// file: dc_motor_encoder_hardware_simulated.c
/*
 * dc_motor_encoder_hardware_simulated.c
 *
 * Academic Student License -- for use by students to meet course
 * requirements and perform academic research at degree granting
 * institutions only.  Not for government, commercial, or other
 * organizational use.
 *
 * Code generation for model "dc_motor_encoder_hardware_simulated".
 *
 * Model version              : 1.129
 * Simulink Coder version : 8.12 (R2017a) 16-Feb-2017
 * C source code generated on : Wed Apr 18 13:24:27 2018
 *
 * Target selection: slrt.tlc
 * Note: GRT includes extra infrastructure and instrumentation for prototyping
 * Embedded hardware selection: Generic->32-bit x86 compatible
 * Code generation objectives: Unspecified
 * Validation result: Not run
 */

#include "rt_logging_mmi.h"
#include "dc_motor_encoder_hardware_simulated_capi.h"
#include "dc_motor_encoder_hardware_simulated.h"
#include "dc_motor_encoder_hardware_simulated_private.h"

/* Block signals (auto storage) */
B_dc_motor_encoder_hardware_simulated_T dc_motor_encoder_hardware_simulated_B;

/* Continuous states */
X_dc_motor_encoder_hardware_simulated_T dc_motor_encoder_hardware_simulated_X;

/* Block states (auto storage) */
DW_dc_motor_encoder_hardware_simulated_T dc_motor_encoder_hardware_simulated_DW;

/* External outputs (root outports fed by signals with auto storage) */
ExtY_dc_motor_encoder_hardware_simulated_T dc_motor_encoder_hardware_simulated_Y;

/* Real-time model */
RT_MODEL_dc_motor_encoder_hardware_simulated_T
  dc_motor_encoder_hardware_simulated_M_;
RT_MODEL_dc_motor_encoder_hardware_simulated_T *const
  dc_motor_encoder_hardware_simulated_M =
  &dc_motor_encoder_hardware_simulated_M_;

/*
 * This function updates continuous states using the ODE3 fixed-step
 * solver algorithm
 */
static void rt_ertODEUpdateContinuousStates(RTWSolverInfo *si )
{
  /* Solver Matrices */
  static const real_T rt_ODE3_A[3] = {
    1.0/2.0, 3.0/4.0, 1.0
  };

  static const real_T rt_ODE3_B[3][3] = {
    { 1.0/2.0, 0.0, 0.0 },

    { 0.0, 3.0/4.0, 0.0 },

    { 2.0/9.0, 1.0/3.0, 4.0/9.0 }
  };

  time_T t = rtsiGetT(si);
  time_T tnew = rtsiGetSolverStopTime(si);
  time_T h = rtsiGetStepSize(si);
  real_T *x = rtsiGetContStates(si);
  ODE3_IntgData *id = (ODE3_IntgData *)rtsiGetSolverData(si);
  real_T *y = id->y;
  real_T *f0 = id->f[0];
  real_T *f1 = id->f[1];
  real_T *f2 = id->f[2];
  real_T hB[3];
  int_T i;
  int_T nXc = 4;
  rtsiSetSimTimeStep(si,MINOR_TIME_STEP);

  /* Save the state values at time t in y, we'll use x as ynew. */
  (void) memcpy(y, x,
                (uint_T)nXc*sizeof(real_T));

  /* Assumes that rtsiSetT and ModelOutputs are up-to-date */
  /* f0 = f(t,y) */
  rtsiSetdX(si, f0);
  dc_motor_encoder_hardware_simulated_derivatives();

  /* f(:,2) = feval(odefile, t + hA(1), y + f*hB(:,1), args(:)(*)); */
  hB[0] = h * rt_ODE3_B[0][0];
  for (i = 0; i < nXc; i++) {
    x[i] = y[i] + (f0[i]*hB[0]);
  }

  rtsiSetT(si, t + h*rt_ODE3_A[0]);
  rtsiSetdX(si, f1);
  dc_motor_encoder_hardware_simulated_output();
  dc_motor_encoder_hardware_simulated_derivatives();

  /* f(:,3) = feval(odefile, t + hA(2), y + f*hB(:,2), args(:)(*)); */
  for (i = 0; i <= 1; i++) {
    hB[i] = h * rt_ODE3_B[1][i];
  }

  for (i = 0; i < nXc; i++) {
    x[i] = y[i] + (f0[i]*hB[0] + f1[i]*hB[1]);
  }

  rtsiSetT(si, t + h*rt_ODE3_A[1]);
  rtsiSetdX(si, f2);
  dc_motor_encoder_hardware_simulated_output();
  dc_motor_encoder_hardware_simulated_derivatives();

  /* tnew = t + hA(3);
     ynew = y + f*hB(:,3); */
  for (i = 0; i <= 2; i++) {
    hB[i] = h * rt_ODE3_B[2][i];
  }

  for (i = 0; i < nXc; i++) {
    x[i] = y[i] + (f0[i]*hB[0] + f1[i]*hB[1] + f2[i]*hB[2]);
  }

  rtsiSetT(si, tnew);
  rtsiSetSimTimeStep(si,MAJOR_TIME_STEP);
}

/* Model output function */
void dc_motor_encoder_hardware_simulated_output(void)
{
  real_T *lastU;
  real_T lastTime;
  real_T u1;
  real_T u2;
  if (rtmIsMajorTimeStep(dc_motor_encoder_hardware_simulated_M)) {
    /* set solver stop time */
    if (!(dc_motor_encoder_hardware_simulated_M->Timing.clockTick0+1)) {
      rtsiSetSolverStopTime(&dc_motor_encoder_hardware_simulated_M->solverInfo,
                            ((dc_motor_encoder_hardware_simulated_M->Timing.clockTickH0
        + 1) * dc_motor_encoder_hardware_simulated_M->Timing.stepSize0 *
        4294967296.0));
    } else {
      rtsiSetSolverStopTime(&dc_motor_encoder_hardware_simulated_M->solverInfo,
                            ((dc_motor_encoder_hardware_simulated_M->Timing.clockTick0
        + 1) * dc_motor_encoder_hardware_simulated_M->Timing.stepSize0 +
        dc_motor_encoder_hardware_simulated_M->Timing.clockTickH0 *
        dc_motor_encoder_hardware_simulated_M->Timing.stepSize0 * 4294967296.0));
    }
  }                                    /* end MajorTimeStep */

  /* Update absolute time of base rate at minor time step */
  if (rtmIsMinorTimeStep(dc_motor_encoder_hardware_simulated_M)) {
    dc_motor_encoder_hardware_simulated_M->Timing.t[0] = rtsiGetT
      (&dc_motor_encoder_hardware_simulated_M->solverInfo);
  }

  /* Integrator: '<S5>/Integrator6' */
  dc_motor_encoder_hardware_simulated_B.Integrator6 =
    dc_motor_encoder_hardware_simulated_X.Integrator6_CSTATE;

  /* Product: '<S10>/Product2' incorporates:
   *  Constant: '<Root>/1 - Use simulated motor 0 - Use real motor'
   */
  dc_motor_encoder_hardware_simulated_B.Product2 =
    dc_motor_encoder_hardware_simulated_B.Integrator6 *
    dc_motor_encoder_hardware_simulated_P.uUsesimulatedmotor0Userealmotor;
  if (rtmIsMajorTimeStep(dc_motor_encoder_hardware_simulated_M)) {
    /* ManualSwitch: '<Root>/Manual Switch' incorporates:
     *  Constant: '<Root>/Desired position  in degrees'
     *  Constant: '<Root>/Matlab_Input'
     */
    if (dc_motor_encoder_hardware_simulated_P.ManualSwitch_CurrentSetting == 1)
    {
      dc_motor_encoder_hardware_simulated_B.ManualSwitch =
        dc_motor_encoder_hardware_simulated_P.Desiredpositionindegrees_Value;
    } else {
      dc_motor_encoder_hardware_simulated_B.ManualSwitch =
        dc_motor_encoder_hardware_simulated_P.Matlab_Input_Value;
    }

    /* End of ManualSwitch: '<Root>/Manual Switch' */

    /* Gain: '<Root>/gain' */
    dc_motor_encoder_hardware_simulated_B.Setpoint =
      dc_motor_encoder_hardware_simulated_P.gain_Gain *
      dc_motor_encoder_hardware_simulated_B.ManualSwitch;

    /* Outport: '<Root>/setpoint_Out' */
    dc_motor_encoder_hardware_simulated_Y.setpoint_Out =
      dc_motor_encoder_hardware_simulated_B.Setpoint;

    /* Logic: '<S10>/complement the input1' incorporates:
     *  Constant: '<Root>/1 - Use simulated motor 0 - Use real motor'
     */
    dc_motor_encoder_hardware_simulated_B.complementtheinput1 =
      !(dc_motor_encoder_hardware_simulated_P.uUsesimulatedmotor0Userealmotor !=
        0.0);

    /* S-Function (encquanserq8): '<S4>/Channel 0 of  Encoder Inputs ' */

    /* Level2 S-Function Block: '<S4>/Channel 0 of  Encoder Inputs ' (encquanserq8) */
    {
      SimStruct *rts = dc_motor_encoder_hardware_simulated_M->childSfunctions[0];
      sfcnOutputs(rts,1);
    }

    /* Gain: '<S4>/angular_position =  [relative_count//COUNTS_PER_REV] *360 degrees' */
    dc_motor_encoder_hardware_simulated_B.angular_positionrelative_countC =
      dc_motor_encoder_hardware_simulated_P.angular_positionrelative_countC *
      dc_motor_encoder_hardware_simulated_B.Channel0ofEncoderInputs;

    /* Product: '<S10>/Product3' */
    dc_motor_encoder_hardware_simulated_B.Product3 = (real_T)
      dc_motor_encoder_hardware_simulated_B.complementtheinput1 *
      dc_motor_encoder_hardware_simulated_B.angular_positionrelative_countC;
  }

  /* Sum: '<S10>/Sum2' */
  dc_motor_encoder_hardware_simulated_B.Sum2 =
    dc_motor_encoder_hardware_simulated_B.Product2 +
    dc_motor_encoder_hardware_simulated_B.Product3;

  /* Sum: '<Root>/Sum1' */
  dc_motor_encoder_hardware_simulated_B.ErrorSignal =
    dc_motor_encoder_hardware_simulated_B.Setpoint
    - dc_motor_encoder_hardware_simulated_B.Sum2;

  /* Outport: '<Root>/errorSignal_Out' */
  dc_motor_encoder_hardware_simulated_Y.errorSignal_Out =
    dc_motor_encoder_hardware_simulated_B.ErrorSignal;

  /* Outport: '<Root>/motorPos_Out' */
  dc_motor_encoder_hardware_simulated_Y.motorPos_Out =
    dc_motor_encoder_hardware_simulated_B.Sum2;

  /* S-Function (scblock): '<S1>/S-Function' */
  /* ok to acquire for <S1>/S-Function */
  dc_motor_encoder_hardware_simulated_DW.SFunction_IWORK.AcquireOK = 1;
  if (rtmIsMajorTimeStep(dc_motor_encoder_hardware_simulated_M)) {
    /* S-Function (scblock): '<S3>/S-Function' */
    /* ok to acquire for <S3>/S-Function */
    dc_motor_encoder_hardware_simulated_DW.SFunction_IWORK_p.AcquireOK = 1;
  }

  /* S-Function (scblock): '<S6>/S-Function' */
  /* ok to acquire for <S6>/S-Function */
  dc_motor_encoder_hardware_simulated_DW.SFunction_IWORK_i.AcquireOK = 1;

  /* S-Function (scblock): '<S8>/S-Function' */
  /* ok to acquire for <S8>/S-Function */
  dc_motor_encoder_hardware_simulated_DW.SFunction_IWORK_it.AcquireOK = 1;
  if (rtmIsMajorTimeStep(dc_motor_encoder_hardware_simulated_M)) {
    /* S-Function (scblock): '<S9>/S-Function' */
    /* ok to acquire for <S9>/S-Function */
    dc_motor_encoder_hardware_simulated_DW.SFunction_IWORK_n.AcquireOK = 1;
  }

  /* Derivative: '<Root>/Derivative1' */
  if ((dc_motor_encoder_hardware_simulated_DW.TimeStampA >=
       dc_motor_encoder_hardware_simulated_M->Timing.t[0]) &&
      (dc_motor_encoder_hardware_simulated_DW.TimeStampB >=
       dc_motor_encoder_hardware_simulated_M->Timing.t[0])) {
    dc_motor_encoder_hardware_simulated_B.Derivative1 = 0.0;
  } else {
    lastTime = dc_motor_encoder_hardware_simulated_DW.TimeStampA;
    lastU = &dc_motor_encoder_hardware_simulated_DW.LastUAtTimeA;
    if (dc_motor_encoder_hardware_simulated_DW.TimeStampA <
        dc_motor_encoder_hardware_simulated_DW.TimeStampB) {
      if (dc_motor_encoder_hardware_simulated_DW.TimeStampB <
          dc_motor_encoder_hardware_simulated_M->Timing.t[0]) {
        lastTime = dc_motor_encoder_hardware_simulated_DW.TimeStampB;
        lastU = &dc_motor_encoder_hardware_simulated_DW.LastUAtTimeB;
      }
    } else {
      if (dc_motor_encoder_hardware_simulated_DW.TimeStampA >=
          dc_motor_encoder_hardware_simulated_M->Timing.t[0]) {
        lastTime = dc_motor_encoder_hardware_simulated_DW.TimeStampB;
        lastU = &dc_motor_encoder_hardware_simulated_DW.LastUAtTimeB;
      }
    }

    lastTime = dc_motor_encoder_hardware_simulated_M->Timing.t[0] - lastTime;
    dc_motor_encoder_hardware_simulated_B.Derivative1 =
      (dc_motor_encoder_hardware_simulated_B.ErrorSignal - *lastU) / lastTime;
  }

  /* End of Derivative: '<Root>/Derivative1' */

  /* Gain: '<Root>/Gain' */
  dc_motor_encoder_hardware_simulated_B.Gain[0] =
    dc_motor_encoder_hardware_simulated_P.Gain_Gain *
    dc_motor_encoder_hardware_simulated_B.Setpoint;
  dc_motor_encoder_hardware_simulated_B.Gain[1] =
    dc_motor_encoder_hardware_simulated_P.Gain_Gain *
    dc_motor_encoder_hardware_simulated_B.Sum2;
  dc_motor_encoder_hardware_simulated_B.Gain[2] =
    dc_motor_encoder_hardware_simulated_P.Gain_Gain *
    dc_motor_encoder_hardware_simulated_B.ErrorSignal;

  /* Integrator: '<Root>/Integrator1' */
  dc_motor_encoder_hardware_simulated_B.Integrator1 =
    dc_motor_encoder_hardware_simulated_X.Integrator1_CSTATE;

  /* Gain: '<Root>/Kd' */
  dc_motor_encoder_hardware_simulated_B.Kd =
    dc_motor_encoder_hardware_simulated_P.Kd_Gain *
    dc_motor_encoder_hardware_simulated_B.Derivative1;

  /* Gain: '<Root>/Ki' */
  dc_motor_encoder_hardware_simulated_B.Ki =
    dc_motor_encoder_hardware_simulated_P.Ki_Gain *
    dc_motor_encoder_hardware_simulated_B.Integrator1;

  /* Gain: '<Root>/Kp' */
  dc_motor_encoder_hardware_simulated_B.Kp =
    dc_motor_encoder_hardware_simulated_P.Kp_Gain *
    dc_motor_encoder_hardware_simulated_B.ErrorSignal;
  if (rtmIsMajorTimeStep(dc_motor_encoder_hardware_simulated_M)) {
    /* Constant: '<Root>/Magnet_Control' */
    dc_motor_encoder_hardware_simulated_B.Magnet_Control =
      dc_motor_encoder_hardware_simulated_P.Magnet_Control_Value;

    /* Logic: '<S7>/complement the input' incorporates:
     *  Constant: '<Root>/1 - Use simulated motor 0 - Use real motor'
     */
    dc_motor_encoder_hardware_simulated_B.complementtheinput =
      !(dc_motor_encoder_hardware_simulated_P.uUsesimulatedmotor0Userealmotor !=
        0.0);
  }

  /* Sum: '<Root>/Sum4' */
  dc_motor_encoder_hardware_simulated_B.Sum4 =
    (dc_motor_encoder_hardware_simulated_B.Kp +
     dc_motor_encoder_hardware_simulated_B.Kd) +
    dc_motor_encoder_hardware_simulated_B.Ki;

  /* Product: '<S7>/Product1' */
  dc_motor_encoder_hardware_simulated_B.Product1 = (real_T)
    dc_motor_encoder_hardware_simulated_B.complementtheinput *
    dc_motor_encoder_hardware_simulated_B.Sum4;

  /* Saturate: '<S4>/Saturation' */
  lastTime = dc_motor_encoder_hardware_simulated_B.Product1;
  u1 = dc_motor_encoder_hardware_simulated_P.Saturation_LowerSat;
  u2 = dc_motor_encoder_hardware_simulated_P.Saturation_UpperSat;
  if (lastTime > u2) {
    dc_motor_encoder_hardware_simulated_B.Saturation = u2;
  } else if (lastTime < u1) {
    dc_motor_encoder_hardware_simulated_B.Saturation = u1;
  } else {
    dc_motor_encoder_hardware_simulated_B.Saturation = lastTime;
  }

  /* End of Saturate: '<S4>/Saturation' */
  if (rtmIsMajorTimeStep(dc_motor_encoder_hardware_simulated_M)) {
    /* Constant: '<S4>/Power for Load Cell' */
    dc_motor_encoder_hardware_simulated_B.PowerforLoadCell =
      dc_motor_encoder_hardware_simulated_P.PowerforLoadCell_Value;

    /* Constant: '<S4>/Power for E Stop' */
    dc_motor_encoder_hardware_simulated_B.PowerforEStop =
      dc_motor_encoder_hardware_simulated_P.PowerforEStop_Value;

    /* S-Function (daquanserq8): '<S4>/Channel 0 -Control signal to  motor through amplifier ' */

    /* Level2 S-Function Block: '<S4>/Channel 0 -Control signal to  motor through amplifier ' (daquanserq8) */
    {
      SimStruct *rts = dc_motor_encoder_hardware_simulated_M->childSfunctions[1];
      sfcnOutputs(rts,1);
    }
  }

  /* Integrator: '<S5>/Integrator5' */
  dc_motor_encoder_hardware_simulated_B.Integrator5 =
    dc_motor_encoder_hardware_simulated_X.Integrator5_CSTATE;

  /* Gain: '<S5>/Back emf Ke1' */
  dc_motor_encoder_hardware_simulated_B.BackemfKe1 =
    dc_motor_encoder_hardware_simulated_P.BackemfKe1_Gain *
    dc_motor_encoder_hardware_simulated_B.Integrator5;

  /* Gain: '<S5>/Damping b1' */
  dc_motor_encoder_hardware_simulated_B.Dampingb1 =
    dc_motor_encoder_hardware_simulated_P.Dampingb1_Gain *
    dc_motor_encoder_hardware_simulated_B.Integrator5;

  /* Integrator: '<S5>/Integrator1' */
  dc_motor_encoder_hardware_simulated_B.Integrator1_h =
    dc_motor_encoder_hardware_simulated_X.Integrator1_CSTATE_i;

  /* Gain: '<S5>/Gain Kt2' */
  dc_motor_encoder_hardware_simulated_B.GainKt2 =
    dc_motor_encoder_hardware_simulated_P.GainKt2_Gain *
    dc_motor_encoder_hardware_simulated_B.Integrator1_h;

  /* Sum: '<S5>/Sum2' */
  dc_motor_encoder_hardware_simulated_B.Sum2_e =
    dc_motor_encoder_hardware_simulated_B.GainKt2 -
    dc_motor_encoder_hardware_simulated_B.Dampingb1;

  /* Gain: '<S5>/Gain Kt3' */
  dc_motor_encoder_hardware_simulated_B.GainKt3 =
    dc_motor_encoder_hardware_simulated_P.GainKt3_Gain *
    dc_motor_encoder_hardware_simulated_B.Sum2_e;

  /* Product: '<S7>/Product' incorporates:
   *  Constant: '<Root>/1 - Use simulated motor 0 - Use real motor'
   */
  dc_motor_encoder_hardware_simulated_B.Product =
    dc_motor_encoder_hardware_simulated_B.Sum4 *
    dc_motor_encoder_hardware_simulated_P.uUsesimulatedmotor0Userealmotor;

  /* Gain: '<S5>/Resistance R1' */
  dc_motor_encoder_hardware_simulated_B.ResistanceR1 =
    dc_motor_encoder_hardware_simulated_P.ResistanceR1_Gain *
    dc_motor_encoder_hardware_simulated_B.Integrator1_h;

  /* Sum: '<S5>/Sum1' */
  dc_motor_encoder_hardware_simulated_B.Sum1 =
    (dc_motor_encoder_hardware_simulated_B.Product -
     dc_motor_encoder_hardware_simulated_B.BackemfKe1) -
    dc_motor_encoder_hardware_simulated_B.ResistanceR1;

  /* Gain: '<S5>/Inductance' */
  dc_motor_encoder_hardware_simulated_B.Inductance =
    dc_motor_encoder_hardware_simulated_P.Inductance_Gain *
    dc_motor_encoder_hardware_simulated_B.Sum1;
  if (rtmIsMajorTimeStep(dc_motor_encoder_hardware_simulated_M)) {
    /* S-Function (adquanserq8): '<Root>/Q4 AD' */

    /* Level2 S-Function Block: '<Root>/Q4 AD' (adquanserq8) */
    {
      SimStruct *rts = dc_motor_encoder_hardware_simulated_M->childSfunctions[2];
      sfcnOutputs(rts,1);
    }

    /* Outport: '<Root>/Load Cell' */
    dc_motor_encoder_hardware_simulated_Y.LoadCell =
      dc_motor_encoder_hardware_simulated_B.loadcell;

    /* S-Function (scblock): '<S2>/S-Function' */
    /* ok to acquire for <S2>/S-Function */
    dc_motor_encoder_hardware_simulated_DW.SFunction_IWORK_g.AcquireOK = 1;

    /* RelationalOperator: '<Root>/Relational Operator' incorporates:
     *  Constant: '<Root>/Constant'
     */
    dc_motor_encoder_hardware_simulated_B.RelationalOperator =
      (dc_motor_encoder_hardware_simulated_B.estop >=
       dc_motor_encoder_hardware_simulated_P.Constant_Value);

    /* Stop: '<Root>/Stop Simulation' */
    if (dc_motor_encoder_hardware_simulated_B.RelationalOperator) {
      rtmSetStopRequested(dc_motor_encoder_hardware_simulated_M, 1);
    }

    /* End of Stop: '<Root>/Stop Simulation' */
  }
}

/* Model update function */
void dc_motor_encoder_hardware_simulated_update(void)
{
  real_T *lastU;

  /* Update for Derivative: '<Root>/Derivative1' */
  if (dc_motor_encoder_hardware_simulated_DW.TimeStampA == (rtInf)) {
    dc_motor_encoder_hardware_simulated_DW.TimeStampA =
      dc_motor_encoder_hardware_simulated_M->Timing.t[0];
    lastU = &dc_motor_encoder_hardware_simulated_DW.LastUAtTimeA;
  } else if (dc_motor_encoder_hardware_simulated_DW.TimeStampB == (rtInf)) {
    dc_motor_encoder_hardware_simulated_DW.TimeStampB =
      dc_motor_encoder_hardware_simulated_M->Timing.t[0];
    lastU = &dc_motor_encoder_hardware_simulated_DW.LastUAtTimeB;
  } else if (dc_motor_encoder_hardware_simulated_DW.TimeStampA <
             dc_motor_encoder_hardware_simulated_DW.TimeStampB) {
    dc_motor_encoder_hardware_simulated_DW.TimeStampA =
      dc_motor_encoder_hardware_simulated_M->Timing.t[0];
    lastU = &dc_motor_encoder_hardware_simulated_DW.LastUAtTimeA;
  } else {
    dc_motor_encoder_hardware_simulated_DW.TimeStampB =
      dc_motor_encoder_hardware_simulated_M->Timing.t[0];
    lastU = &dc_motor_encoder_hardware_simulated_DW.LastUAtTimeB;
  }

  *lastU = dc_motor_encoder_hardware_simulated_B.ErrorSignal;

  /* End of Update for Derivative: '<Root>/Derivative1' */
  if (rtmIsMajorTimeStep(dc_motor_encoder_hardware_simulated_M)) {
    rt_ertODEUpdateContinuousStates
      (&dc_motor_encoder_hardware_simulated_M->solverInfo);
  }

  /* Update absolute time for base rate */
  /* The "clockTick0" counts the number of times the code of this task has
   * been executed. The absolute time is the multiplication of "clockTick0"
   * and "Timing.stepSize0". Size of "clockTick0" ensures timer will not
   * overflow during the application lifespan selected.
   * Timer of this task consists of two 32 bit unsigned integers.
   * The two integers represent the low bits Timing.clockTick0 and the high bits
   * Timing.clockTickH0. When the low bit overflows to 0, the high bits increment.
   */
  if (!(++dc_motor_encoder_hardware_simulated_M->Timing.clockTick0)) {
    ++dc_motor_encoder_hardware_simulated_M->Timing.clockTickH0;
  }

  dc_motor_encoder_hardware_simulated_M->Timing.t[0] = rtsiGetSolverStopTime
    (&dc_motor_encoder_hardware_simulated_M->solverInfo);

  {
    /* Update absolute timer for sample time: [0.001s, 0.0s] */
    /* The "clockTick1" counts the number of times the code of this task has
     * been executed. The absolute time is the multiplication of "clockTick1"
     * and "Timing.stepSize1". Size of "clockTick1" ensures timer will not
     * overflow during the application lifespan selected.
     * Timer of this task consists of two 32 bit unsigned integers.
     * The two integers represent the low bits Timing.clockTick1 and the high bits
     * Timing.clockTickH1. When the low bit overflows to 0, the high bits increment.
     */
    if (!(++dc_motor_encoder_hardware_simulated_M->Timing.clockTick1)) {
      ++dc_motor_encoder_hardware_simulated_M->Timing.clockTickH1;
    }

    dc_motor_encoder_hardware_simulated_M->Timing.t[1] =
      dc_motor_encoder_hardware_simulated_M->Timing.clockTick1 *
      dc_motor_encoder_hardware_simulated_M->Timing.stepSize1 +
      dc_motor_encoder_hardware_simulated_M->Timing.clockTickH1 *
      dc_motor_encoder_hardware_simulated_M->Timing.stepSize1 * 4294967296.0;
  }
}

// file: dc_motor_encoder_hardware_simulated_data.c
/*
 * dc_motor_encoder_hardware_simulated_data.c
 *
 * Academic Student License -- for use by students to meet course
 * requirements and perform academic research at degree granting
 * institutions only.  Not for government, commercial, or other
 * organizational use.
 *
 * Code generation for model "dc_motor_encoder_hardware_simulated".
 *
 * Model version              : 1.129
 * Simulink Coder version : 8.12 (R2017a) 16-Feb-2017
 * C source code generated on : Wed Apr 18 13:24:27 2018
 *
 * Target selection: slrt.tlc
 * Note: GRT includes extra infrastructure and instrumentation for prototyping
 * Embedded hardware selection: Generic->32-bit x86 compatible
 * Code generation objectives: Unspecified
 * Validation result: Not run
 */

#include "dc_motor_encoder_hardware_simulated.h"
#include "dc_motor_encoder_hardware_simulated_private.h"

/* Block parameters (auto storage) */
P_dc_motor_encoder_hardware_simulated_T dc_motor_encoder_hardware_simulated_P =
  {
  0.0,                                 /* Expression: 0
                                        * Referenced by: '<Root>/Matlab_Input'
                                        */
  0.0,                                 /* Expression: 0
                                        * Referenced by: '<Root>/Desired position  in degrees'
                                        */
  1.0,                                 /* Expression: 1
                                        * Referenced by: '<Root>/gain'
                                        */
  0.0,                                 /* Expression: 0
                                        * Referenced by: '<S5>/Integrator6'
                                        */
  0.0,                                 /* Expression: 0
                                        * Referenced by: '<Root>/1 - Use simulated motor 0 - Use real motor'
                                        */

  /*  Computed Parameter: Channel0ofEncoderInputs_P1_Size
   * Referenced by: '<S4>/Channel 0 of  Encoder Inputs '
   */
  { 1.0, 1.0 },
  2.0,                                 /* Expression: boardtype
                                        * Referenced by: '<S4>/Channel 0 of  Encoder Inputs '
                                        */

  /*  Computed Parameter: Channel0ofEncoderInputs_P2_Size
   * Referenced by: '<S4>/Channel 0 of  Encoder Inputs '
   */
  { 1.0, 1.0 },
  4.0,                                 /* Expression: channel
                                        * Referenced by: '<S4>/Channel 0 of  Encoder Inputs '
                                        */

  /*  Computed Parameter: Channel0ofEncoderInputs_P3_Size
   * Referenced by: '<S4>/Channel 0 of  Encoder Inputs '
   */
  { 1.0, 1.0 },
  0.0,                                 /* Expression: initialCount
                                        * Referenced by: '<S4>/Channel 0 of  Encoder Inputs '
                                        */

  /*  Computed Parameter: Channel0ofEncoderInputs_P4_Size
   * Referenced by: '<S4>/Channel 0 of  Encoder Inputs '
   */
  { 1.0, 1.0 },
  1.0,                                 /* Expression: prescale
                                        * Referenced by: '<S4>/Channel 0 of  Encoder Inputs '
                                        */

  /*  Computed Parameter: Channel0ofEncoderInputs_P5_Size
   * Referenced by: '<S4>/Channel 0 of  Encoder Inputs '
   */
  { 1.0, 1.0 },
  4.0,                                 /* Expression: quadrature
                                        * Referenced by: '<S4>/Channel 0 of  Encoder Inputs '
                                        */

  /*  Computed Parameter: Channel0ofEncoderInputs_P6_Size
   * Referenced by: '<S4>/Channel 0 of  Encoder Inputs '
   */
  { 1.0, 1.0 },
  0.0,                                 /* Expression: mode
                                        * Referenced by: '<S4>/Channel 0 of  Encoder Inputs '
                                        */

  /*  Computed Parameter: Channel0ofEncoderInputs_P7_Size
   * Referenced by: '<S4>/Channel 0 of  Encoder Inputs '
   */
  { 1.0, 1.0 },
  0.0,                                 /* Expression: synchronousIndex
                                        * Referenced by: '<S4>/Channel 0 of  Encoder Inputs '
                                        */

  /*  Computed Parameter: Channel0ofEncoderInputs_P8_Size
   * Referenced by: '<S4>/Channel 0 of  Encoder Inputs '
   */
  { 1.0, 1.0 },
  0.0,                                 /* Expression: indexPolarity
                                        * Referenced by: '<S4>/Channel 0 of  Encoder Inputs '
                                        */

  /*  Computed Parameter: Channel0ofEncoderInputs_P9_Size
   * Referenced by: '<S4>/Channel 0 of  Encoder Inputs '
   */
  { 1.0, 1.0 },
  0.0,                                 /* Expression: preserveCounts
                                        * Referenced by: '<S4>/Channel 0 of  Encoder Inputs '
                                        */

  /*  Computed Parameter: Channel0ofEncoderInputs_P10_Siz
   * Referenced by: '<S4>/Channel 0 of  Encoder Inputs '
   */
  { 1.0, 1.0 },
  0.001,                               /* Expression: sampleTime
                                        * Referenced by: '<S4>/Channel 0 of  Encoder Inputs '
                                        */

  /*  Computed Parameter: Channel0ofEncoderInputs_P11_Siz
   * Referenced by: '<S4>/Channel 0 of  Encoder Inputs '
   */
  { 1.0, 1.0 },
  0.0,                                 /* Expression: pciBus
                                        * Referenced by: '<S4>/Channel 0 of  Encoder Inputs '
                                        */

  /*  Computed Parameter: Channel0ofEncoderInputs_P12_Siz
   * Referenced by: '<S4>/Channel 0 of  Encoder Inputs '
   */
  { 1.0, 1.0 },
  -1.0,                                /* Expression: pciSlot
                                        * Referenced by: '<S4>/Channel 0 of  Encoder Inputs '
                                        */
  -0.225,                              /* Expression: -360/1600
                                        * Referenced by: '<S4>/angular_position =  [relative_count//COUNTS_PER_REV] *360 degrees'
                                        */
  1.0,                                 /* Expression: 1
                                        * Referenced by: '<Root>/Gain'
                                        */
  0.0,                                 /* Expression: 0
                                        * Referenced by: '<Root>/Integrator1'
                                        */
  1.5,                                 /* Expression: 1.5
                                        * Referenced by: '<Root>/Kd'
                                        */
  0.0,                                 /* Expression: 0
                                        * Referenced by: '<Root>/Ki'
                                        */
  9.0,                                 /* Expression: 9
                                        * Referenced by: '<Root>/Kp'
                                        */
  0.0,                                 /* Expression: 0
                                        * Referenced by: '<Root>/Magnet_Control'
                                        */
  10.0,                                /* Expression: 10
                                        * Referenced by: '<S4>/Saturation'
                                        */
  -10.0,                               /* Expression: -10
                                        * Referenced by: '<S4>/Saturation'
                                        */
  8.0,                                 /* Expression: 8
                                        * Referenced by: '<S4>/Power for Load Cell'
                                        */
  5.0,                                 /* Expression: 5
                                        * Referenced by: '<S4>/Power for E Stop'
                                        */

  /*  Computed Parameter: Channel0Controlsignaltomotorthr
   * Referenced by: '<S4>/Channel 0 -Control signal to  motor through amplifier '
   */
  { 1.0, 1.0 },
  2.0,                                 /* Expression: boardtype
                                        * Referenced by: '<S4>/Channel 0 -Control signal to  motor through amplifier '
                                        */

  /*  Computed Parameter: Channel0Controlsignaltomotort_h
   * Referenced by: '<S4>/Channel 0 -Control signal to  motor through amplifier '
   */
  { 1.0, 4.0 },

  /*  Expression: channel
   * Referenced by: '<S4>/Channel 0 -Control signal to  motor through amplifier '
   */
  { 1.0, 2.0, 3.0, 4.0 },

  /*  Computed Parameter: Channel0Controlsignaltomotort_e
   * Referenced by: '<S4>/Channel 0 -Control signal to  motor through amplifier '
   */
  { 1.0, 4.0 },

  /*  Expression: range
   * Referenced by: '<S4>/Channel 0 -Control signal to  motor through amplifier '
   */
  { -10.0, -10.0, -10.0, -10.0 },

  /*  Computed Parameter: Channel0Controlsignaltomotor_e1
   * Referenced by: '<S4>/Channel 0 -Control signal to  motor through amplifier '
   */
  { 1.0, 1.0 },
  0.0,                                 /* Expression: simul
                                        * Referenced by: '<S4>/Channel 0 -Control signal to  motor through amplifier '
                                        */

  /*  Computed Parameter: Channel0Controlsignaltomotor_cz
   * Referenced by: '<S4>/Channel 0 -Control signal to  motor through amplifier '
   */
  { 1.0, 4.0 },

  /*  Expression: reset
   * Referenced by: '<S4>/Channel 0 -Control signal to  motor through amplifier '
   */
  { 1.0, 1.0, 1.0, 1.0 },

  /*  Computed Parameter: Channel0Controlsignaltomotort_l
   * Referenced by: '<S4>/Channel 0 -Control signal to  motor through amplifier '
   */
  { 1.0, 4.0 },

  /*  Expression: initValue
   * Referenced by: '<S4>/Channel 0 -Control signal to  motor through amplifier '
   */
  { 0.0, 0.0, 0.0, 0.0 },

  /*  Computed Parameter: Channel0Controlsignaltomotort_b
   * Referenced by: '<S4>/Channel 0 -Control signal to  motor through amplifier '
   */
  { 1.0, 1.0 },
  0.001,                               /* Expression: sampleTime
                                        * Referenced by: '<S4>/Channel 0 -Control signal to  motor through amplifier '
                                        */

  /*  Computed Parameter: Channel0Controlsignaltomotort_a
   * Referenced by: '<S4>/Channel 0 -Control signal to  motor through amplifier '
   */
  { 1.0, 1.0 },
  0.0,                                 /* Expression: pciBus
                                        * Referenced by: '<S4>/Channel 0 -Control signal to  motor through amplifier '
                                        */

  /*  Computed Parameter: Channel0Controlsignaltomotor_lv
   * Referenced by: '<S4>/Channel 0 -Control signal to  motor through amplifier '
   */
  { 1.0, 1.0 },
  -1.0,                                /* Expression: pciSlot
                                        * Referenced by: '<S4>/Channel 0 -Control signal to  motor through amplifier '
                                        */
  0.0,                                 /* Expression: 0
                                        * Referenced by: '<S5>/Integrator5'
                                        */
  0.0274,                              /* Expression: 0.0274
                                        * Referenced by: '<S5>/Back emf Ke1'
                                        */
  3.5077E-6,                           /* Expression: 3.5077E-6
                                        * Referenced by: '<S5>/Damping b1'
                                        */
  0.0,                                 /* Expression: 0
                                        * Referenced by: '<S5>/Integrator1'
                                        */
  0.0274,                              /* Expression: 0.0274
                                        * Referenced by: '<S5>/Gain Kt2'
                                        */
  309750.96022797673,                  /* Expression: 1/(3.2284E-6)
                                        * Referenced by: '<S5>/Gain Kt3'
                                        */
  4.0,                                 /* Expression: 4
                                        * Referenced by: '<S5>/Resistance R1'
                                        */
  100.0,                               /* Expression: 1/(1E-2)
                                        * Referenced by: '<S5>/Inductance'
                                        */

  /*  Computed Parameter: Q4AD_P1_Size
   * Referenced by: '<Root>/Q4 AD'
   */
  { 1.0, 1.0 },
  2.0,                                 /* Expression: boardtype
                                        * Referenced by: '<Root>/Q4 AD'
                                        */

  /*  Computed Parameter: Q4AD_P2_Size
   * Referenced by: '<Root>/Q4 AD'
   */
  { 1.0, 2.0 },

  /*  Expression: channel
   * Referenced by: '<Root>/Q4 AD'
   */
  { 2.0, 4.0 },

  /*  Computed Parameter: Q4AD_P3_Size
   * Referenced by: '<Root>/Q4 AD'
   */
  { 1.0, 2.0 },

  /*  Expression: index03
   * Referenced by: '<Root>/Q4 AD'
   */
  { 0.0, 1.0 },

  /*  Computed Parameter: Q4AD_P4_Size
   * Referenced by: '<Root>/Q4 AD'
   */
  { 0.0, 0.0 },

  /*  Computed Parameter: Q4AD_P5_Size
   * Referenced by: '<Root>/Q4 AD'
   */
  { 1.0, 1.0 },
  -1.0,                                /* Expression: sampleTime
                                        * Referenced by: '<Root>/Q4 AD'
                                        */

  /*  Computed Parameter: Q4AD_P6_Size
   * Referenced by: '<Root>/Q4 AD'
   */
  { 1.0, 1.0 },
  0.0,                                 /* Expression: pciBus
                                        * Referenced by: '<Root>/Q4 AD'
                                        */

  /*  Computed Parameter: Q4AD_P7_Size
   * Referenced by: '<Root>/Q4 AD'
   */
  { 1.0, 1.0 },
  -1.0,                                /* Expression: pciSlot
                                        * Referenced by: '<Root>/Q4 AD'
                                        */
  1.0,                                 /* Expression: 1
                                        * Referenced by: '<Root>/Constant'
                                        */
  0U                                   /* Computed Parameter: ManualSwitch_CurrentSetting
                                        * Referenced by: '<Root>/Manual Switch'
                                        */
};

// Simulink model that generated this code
simulink model "dc_motor_encoder_hardware_simulated"  (Simulink 8.9)
settings: Solver=ode3  StartTime=0.0  StopTime=inf  FixedStep=0.001  RelTol=1e-3  EnableMultiTasking=on
libraries: slrtlib x6, xpcquanserlib x3

== system dc_motor_encoder_hardware_simulated ==
  note: Adjust these gains and observe the change of the
      | motor response on the Error and Motor Position
      | plots.
  note: First, test the control inputs on the simulated motor and
      | adjust gains according to the response. Then, flip the switch and
      | test with the real motor in the loop
  note: Switch
  1 - Use simulated motor 0 - Use real motor : Constant  Value=0
  Constant : Constant
  Data Display : slrtlib/Displays and Logging/Scope   scopeno=3  scopetype=Target  autostart=on  viewmode=Numerical  formatstr="'Setpoint        %3.2f,Motor Position  %3.2f,Error Signal    %3.2f'"  grid=on  ylimits=[0,170]  nosamples=200  noprepostsamples=0  interleave=10  triggermode=FreeRun  triggersignal=1  trigsignalfromport=off  triggerlevel=0.0  triggerslope=Either  triggerscope=1  triggersample=0  filename=data.dat  mode=Lazy  writesize=512  autorestart=off  dynamicfilemode=off  maxwritefilesize=512*1024^2
  Derivative1 : Derivative
  Desired position  in degrees : Constant  Value=0
  Gain : Gain
  Integrator1 : Integrator
  Kd : Gain  Gain=1.5
  Ki : Gain  Gain=0
  Kp : Gain  Gain=9
  "Load Cell Scope " : slrtlib/Displays and Logging/Scope   scopeno=5  scopetype=Target  autostart=on  viewmode=Graphical redraw  formatstr='%15.6f'  grid=on  ylimits=[0,2]  nosamples=200  noprepostsamples=0  interleave=1  triggermode=FreeRun  triggersignal=1  trigsignalfromport=off  triggerlevel=0.0  triggerslope=Either  triggerscope=1  triggersample=0  filename=data.dat  mode=Lazy  writesize=512  autorestart=off  dynamicfilemode=off  maxwritefilesize=512*1024^2
  Magnet Control Scope : slrtlib/Displays and Logging/Scope   scopeno=4  scopetype=Target  autostart=on  viewmode=Graphical redraw  formatstr='%15.6f'  grid=on  ylimits=[0,2]  nosamples=200  noprepostsamples=0  interleave=1  triggermode=FreeRun  triggersignal=1  trigsignalfromport=off  triggerlevel=0.0  triggerslope=Either  triggerscope=1  triggersample=0  filename=data.dat  mode=Lazy  writesize=512  autorestart=off  dynamicfilemode=off  maxwritefilesize=512*1024^2
  Magnet_Control : Constant  Value=0
  Manual Switch : ManualSwitch  CurrentSetting=0
  Matlab_Input : Constant  Value=0
  Mux : Mux  Inputs=3
  Q4 AD : xpcquanserlib/A//D/Q4 AD  channel=[2 4]  sampleTime=-1  slot=-1
  Real motor : Subsystem
  Relational Operator : RelationalOperator  OutDataTypeStr=boolean  RndMeth=Nearest
  Simulated motor : Subsystem
  Stop Simulation : Stop
  Sum1 : Sum  Inputs=|+-
  Sum4 : Sum  Inputs=||+++
  error signal : slrtlib/Displays and Logging/Scope   scopeno=2  scopetype=Target  autostart=on  viewmode=Graphical rolling  formatstr='%15.6f'  grid=on  ylimits=[-180,180]  nosamples=500  noprepostsamples=0  interleave=10  triggermode=FreeRun  triggersignal=1  trigsignalfromport=off  triggerlevel=0.0  triggerslope=Either  triggerscope=1  triggersample=0  filename=data.dat  mode=Lazy  writesize=512  autorestart=off  dynamicfilemode=off  maxwritefilesize=512*1024^2
  gain : Gain
  input side switching logic : Subsystem
  motor position : slrtlib/Displays and Logging/Scope   scopeno=7  scopetype=Target  autostart=on  viewmode=Graphical rolling  formatstr='%15.6f'  grid=on  ylimits=[-180,180]  nosamples=500  noprepostsamples=0  interleave=10  triggermode=FreeRun  triggersignal=1  trigsignalfromport=off  triggerlevel=0.0  triggerslope=Either  triggerscope=1  triggersample=0  filename=data.dat  mode=Lazy  writesize=512  autorestart=off  dynamicfilemode=off  maxwritefilesize=512*1024^2
  setpoint : slrtlib/Displays and Logging/Scope   scopeno=1  scopetype=Target  autostart=on  viewmode=Graphical rolling  formatstr='%15.6f'  grid=on  ylimits=[-180,180]  nosamples=500  noprepostsamples=0  interleave=10  triggermode=FreeRun  triggersignal=1  trigsignalfromport=off  triggerlevel=0.0  triggerslope=Either  triggerscope=1  triggersample=0  filename=data.dat  mode=Lazy  writesize=512  autorestart=off  dynamicfilemode=off  maxwritefilesize=512*1024^2
  switching logic : Subsystem
  setpoint_Out : Outport
  errorSignal_Out : Outport  Port=2
  motorPos_Out : Outport  Port=3  SignalName=name
  Load Cell : Outport  Port=4
  wires:
  Kp/1 -> Sum4/1
  Kd/1 -> Sum4/2
  Derivative1/1 -> Kd/1
  Integrator1/1 -> Ki/1
  Ki/1 -> Sum4/3
  gain/1 -> Sum1/1, Mux/1, setpoint/1, setpoint_Out/1  "Setpoint"
  input side switching logic/1(Simulated) -> Simulated motor/1(control  input)
  input side switching logic/2(Real) -> Real motor/1(unfiltered  control input)
  Simulated motor/1(position) -> switching logic/1(simulated)
  Real motor/1(position in degrees) -> switching logic/3(real)
  switching logic/1(position) -> Mux/2, Sum1/2, motor position/1, motorPos_Out/1  "Motor Position"
  Sum4/1 -> input side switching logic/1(control input)
  1 - Use simulated motor 0 - Use real motor/1 -> input side switching logic/2(switch  position), switching logic/2(switch position)
  Gain/1 -> Data Display/1
  Mux/1 -> Gain/1
  Sum1/1 -> Kp/1, Derivative1/1, Integrator1/1, Mux/3, error signal/1, errorSignal_Out/1  "Error Signal"
  Desired position  in degrees/1 -> Manual Switch/1
  Manual Switch/1 -> gain/1
  Matlab_Input/1 -> Manual Switch/2
  Magnet_Control/1 -> Real motor/2("Electromagnet input "), Magnet Control Scope/1
  Q4 AD/1 -> "Load Cell Scope "/1, Load Cell/1  "loadcell"
  Constant/1 -> Relational Operator/2
  Relational Operator/1 -> Stop Simulation/1
  Q4 AD/2 -> Relational Operator/1  "estop"

== system dc_motor_encoder_hardware_simulated/Real motor ==
  note: Saturation
  note: External connections to and from the motor using the Q4.
      |
      | Encoder feedback is scaled using the modulus and Gain blocks to
      | match the range of the Desired Trajectory input.
      |
      | In this example need to convert the encoder counts to a value between 0 and COUNTS_PER_REV.
      | Further, the count obtained for that revolution needs to be scaled to an angle feedback (between
      | 0 and 360 degrees), which is the purpose of the Gain block.
  unfiltered  control input : Inport
  "Electromagnet input " : Inport  Port=2
  "Channel 0 -Control signal to  motor through amplifier " : xpcquanserlib/D//A/Q4 DA   channel=[1 2 3 4]  range=[-10]  simul=off  reset=[1]  initValue=[0]  sampleTime=.001  slot=-1
  "Channel 0 of  Encoder Inputs " : xpcquanserlib/Incremental Encoder/Q4 Enc   channel=[4]  initialCount=[0]  prescale=[1]  quadrature=[4]  mode=[0]  synchronousIndex=[0]  indexPolarity=[0]  preserveCounts=[0]  sampleTime=.001  slot=-1
  Power for E Stop : Constant  Value=5
  Power for Load Cell : Constant  Value=8
  Saturation : Saturate  UpperLimit=10  LowerLimit=-10
  angular_position =  [relative_count/COUNTS_PER_REV] *360 degrees : Gain  Gain=-360/1600
  position in degrees : Outport
  wires:
  Saturation/1 -> "Channel 0 -Control signal to  motor through amplifier "/1
  angular_position =  [relative_count/COUNTS_PER_REV] *360 degrees/1 -> position in degrees/1
  "Channel 0 of  Encoder Inputs "/1 -> angular_position =  [relative_count/COUNTS_PER_REV] *360 degrees/1
  unfiltered  control input/1 -> Saturation/1
  "Electromagnet input "/1 -> "Channel 0 -Control signal to  motor through amplifier "/2
  Power for E Stop/1 -> "Channel 0 -Control signal to  motor through amplifier "/4
  Power for Load Cell/1 -> "Channel 0 -Control signal to  motor through amplifier "/3

== system dc_motor_encoder_hardware_simulated/Simulated motor ==
  control  input : Inport
  Back emf Ke1 : Gain  Gain=0.0274
  Damping b1 : Gain  Gain=3.5077E-6
  Gain Kt2 : Gain  Gain=0.0274
  Gain Kt3 : Gain  Gain=1/(3.2284E-6)
  Inductance : Gain  Gain=1/(1E-2)
  Integrator1 : Integrator
  Integrator5 : Integrator
  Integrator6 : Integrator
  Resistance R1 : Gain  Gain=4
  Sum1 : Sum  Inputs=||+--
  Sum2 : Sum  Inputs=|+-
  position : Outport
  wires:
  Sum1/1 -> Inductance/1
  Inductance/1 -> Integrator1/1
  Integrator1/1 -> Gain Kt2/1, Resistance R1/1
  Gain Kt2/1 -> Sum2/1
  Sum2/1 -> Gain Kt3/1
  Gain Kt3/1 -> Integrator5/1
  Integrator5/1 -> Integrator6/1, Back emf Ke1/1, Damping b1/1
  Back emf Ke1/1 -> Sum1/2
  Damping b1/1 -> Sum2/2
  Resistance R1/1 -> Sum1/3
  Integrator6/1 -> position/1
  control  input/1 -> Sum1/1

== system dc_motor_encoder_hardware_simulated/input side switching logic ==
  control input : Inport
  switch  position : Inport  Port=2
  Product : Product  RndMeth=Zero
  Product1 : Product  RndMeth=Zero
  complement the input : Logic  Operator=NOT  AllPortsSameDT=off  OutDataTypeStr=boolean
  Simulated : Outport
  Real : Outport  Port=2
  wires:
  control input/1 -> Product/1, Product1/2
  complement the input/1 -> Product1/1
  switch  position/1 -> Product/2, complement the input/1
  Product/1 -> Simulated/1
  Product1/1 -> Real/1

== system dc_motor_encoder_hardware_simulated/switching logic ==
  simulated : Inport
  switch position : Inport  Port=2
  real : Inport  Port=3
  Product2 : Product  RndMeth=Zero
  Product3 : Product  RndMeth=Zero
  Sum2 : Sum  Inputs=|++
  complement the input1 : Logic  Operator=NOT  AllPortsSameDT=off  OutDataTypeStr=boolean
  position : Outport
  wires:
  complement the input1/1 -> Product3/1
  Product2/1 -> Sum2/1
  Product3/1 -> Sum2/2
  switch position/1 -> Product2/2, complement the input1/1
  simulated/1 -> Product2/1
  Sum2/1 -> position/1
  real/1 -> Product3/2
